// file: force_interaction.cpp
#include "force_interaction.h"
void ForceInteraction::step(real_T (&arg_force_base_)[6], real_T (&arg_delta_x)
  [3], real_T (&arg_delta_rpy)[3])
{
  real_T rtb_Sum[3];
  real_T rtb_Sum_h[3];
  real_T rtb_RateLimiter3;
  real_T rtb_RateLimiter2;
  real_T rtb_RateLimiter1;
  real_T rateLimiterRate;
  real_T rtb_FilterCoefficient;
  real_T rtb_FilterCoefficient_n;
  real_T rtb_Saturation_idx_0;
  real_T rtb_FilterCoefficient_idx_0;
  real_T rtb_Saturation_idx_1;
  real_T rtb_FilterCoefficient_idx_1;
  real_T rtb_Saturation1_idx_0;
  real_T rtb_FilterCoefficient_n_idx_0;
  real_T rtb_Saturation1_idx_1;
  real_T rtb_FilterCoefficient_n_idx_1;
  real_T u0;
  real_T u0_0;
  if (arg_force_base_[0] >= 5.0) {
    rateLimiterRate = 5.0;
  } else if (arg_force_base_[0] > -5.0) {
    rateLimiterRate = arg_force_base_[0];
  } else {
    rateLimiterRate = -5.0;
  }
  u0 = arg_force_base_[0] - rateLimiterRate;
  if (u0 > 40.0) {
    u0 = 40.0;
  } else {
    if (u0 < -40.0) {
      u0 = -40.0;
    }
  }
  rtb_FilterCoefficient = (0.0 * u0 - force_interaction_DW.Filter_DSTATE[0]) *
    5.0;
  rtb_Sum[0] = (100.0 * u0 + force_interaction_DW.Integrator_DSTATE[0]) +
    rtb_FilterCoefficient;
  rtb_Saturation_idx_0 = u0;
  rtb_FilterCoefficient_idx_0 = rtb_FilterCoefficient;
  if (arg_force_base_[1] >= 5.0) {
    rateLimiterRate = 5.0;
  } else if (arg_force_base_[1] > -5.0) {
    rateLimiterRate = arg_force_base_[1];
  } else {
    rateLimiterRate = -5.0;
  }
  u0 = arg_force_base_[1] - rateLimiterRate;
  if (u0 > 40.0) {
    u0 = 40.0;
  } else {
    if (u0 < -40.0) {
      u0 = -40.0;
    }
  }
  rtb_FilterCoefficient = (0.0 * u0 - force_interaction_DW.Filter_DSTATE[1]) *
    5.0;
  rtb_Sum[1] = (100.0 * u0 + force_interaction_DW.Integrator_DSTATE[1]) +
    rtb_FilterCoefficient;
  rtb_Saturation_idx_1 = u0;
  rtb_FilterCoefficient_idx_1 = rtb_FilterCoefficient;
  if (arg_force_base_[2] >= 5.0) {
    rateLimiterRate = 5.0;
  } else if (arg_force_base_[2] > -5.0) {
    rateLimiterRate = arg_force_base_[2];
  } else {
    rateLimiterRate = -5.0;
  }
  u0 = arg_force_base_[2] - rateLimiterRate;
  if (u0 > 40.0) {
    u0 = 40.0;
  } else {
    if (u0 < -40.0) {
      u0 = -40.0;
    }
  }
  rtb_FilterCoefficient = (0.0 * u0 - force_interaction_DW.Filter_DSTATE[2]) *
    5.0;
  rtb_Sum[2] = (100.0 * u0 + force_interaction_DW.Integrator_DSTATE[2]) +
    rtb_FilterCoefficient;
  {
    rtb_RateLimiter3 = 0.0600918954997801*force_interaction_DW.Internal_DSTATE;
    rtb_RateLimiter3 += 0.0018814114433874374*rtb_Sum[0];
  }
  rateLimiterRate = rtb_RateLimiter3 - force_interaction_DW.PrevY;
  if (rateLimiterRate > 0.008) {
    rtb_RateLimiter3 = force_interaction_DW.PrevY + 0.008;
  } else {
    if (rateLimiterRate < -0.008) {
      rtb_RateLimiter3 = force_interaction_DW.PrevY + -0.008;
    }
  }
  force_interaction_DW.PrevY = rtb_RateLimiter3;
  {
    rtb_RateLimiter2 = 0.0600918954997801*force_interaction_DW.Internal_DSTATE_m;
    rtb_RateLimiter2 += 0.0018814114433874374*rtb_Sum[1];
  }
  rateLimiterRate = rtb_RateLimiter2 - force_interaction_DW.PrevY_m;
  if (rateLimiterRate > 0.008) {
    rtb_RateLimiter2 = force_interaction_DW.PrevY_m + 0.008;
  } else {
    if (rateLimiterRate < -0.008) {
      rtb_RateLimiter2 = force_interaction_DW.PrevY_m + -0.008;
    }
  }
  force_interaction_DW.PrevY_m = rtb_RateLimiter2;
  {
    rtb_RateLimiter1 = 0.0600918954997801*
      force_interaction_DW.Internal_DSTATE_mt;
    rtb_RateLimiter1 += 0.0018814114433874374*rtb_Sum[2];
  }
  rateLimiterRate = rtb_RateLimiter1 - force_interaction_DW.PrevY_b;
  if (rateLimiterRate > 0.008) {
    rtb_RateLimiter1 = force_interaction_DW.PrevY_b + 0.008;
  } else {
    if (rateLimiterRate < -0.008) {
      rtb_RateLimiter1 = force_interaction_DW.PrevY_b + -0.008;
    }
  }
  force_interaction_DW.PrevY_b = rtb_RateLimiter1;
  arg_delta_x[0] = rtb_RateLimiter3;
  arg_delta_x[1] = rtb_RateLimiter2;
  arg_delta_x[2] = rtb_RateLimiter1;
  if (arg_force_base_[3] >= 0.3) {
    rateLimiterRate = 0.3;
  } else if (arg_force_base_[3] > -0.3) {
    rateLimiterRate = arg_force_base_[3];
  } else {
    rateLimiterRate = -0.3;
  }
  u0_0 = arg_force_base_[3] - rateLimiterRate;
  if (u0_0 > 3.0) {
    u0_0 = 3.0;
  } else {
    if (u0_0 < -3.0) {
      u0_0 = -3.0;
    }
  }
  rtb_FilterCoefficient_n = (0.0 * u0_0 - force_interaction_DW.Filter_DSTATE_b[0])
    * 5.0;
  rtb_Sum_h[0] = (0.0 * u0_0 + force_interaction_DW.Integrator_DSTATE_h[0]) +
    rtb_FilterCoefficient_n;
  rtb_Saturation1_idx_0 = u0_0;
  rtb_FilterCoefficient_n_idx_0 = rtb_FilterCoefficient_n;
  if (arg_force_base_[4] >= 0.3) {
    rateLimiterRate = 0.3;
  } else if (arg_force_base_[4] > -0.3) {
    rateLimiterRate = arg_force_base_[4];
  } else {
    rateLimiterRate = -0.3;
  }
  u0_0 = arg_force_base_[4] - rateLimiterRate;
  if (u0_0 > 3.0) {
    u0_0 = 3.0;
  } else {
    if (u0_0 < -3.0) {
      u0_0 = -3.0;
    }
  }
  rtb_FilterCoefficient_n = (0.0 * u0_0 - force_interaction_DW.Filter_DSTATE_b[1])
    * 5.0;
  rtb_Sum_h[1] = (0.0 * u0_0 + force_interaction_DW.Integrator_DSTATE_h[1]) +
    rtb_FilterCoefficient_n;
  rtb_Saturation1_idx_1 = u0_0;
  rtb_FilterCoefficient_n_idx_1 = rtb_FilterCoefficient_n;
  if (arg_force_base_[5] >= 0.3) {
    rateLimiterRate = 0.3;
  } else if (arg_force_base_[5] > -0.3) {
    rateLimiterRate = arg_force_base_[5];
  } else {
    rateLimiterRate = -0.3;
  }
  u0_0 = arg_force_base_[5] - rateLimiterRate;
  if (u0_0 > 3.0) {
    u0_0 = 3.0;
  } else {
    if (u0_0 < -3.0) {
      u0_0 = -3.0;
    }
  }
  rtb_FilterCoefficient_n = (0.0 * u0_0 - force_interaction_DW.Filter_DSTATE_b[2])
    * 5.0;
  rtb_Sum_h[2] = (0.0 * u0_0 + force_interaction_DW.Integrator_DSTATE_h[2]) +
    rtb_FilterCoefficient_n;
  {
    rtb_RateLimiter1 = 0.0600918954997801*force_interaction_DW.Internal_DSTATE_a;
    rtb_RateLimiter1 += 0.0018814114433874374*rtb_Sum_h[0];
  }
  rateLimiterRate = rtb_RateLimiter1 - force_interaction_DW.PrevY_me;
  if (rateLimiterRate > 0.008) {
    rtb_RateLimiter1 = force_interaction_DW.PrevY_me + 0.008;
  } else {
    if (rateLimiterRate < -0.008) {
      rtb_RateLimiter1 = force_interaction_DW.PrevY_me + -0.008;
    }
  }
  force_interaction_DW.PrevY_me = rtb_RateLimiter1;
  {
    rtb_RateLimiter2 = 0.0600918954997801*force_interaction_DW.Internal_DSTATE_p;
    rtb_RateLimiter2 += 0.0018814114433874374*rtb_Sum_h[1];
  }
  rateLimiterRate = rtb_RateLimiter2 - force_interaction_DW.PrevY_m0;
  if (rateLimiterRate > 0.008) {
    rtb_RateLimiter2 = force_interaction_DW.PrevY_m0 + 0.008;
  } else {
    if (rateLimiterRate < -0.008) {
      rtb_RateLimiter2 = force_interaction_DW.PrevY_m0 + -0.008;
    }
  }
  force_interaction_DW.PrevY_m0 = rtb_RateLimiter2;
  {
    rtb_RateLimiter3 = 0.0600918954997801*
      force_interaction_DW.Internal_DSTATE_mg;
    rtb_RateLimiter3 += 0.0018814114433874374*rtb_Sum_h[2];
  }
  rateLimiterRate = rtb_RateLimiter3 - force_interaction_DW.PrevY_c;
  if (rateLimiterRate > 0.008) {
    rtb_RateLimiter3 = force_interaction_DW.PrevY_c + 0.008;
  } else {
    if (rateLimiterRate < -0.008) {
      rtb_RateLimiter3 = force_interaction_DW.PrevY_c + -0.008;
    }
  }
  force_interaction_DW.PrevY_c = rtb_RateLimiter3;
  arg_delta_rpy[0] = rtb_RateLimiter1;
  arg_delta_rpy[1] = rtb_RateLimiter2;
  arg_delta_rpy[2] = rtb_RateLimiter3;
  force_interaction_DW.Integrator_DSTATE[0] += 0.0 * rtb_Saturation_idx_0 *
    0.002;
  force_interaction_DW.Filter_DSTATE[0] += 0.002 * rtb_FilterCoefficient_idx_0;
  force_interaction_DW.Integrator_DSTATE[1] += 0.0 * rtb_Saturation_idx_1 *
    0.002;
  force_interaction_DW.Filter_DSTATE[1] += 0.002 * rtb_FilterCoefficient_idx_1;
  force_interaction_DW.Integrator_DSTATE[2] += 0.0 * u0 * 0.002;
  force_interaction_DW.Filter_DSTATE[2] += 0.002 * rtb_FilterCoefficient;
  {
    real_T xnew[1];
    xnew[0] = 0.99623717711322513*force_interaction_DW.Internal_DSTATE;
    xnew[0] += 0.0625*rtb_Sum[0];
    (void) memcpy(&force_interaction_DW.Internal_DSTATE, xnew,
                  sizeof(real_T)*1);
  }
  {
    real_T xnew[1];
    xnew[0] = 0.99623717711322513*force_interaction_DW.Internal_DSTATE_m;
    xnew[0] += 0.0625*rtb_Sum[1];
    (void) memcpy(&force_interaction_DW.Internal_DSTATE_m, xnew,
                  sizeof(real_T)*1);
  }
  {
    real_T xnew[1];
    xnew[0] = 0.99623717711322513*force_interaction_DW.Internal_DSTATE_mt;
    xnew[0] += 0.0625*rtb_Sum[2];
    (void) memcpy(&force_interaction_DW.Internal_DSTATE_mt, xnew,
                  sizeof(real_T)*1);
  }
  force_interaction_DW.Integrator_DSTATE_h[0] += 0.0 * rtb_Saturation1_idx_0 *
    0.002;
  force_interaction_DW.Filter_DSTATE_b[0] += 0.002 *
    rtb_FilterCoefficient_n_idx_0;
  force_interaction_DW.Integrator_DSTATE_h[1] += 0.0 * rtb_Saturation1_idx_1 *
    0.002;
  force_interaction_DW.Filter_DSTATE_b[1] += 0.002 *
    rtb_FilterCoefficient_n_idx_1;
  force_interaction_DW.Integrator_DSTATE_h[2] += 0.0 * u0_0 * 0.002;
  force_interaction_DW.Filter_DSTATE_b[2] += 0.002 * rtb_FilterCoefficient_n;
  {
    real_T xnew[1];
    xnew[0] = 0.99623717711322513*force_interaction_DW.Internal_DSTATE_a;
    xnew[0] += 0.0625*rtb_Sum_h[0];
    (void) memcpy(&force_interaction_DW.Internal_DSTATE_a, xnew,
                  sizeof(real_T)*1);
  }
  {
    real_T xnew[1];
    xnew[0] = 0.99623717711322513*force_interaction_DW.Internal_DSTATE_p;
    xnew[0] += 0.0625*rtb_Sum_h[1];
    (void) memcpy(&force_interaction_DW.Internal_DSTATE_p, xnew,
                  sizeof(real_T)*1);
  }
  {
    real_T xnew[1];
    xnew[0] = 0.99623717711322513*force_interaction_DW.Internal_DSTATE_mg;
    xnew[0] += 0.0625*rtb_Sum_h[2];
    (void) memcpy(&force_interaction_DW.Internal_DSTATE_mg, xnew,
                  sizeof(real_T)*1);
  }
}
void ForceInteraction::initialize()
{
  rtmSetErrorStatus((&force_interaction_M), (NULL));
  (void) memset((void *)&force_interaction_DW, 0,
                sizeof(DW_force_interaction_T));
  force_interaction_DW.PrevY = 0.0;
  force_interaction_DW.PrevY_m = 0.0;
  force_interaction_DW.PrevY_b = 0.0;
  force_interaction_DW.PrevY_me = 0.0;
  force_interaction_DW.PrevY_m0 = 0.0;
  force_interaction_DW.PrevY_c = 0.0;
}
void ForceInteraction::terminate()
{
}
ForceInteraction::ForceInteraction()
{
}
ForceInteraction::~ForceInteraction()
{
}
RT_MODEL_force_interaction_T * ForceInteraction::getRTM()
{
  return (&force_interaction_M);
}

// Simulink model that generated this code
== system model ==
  force_base_ : Inport
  delta_x : Outport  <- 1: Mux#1
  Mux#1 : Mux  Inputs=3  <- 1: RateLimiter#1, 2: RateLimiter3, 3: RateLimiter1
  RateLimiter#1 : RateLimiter  RisingSlewLimit=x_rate  FallingSlewLimit=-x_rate  <- 1: LTISystem#1
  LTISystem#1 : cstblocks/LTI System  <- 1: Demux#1
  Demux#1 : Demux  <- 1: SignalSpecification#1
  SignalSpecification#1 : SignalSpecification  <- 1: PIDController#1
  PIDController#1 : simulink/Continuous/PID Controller  Controller=PID  TimeDomain=Discrete-time  IntegratorMethod=Forward Euler  Form=Parallel  P=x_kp  I=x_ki  D=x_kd  N=5  InitialConditionForIntegrator=0  ExternalReset=none  LimitOutput=off  UpperSaturationLimit=inf  LowerSaturationLimit=-inf  <- 1: Saturation
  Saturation : Saturate  UpperLimit=40  LowerLimit=-40  <- 1: DeadZoneDynamic#1
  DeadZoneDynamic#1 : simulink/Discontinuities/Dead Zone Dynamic  <- 1: Constant#1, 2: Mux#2, 3: Constant#2
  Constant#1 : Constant  Value=5
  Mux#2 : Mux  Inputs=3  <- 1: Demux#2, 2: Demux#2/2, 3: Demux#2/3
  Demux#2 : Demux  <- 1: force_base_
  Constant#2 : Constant  Value=-5
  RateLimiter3 : RateLimiter  RisingSlewLimit=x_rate  FallingSlewLimit=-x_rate  <- 1: LTISystem#2
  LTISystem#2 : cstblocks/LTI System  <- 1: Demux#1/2
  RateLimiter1 : RateLimiter  RisingSlewLimit=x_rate  FallingSlewLimit=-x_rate  <- 1: LTISystem#3
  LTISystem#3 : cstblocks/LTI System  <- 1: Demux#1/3
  delta_rpy : Outport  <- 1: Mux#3
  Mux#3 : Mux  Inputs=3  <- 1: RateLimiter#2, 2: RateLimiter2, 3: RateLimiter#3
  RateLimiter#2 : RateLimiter  RisingSlewLimit=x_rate  FallingSlewLimit=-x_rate  <- 1: LTISystem#4
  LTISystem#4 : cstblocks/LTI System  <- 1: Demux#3
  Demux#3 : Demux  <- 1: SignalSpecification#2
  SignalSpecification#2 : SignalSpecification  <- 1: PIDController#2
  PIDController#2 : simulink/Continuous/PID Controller  Controller=PID  TimeDomain=Discrete-time  IntegratorMethod=Forward Euler  Form=Parallel  P=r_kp  I=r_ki  D=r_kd  N=5  InitialConditionForIntegrator=0  ExternalReset=none  LimitOutput=off  UpperSaturationLimit=inf  LowerSaturationLimit=-inf  <- 1: Saturation1
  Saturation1 : Saturate  UpperLimit=3  LowerLimit=-3  <- 1: DeadZoneDynamic#2
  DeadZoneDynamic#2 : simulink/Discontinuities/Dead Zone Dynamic  <- 1: Constant#3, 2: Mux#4, 3: Constant#4
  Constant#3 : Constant  Value=0.3
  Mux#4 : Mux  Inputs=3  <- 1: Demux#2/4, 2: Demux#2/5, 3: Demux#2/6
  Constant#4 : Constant  Value=-0.3
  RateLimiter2 : RateLimiter  RisingSlewLimit=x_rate  FallingSlewLimit=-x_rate  <- 1: LTISystem#5
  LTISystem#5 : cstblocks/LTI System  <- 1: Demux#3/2
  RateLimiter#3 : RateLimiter  RisingSlewLimit=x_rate  FallingSlewLimit=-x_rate  <- 1: LTISystem#6
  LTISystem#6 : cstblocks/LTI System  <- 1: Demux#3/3
